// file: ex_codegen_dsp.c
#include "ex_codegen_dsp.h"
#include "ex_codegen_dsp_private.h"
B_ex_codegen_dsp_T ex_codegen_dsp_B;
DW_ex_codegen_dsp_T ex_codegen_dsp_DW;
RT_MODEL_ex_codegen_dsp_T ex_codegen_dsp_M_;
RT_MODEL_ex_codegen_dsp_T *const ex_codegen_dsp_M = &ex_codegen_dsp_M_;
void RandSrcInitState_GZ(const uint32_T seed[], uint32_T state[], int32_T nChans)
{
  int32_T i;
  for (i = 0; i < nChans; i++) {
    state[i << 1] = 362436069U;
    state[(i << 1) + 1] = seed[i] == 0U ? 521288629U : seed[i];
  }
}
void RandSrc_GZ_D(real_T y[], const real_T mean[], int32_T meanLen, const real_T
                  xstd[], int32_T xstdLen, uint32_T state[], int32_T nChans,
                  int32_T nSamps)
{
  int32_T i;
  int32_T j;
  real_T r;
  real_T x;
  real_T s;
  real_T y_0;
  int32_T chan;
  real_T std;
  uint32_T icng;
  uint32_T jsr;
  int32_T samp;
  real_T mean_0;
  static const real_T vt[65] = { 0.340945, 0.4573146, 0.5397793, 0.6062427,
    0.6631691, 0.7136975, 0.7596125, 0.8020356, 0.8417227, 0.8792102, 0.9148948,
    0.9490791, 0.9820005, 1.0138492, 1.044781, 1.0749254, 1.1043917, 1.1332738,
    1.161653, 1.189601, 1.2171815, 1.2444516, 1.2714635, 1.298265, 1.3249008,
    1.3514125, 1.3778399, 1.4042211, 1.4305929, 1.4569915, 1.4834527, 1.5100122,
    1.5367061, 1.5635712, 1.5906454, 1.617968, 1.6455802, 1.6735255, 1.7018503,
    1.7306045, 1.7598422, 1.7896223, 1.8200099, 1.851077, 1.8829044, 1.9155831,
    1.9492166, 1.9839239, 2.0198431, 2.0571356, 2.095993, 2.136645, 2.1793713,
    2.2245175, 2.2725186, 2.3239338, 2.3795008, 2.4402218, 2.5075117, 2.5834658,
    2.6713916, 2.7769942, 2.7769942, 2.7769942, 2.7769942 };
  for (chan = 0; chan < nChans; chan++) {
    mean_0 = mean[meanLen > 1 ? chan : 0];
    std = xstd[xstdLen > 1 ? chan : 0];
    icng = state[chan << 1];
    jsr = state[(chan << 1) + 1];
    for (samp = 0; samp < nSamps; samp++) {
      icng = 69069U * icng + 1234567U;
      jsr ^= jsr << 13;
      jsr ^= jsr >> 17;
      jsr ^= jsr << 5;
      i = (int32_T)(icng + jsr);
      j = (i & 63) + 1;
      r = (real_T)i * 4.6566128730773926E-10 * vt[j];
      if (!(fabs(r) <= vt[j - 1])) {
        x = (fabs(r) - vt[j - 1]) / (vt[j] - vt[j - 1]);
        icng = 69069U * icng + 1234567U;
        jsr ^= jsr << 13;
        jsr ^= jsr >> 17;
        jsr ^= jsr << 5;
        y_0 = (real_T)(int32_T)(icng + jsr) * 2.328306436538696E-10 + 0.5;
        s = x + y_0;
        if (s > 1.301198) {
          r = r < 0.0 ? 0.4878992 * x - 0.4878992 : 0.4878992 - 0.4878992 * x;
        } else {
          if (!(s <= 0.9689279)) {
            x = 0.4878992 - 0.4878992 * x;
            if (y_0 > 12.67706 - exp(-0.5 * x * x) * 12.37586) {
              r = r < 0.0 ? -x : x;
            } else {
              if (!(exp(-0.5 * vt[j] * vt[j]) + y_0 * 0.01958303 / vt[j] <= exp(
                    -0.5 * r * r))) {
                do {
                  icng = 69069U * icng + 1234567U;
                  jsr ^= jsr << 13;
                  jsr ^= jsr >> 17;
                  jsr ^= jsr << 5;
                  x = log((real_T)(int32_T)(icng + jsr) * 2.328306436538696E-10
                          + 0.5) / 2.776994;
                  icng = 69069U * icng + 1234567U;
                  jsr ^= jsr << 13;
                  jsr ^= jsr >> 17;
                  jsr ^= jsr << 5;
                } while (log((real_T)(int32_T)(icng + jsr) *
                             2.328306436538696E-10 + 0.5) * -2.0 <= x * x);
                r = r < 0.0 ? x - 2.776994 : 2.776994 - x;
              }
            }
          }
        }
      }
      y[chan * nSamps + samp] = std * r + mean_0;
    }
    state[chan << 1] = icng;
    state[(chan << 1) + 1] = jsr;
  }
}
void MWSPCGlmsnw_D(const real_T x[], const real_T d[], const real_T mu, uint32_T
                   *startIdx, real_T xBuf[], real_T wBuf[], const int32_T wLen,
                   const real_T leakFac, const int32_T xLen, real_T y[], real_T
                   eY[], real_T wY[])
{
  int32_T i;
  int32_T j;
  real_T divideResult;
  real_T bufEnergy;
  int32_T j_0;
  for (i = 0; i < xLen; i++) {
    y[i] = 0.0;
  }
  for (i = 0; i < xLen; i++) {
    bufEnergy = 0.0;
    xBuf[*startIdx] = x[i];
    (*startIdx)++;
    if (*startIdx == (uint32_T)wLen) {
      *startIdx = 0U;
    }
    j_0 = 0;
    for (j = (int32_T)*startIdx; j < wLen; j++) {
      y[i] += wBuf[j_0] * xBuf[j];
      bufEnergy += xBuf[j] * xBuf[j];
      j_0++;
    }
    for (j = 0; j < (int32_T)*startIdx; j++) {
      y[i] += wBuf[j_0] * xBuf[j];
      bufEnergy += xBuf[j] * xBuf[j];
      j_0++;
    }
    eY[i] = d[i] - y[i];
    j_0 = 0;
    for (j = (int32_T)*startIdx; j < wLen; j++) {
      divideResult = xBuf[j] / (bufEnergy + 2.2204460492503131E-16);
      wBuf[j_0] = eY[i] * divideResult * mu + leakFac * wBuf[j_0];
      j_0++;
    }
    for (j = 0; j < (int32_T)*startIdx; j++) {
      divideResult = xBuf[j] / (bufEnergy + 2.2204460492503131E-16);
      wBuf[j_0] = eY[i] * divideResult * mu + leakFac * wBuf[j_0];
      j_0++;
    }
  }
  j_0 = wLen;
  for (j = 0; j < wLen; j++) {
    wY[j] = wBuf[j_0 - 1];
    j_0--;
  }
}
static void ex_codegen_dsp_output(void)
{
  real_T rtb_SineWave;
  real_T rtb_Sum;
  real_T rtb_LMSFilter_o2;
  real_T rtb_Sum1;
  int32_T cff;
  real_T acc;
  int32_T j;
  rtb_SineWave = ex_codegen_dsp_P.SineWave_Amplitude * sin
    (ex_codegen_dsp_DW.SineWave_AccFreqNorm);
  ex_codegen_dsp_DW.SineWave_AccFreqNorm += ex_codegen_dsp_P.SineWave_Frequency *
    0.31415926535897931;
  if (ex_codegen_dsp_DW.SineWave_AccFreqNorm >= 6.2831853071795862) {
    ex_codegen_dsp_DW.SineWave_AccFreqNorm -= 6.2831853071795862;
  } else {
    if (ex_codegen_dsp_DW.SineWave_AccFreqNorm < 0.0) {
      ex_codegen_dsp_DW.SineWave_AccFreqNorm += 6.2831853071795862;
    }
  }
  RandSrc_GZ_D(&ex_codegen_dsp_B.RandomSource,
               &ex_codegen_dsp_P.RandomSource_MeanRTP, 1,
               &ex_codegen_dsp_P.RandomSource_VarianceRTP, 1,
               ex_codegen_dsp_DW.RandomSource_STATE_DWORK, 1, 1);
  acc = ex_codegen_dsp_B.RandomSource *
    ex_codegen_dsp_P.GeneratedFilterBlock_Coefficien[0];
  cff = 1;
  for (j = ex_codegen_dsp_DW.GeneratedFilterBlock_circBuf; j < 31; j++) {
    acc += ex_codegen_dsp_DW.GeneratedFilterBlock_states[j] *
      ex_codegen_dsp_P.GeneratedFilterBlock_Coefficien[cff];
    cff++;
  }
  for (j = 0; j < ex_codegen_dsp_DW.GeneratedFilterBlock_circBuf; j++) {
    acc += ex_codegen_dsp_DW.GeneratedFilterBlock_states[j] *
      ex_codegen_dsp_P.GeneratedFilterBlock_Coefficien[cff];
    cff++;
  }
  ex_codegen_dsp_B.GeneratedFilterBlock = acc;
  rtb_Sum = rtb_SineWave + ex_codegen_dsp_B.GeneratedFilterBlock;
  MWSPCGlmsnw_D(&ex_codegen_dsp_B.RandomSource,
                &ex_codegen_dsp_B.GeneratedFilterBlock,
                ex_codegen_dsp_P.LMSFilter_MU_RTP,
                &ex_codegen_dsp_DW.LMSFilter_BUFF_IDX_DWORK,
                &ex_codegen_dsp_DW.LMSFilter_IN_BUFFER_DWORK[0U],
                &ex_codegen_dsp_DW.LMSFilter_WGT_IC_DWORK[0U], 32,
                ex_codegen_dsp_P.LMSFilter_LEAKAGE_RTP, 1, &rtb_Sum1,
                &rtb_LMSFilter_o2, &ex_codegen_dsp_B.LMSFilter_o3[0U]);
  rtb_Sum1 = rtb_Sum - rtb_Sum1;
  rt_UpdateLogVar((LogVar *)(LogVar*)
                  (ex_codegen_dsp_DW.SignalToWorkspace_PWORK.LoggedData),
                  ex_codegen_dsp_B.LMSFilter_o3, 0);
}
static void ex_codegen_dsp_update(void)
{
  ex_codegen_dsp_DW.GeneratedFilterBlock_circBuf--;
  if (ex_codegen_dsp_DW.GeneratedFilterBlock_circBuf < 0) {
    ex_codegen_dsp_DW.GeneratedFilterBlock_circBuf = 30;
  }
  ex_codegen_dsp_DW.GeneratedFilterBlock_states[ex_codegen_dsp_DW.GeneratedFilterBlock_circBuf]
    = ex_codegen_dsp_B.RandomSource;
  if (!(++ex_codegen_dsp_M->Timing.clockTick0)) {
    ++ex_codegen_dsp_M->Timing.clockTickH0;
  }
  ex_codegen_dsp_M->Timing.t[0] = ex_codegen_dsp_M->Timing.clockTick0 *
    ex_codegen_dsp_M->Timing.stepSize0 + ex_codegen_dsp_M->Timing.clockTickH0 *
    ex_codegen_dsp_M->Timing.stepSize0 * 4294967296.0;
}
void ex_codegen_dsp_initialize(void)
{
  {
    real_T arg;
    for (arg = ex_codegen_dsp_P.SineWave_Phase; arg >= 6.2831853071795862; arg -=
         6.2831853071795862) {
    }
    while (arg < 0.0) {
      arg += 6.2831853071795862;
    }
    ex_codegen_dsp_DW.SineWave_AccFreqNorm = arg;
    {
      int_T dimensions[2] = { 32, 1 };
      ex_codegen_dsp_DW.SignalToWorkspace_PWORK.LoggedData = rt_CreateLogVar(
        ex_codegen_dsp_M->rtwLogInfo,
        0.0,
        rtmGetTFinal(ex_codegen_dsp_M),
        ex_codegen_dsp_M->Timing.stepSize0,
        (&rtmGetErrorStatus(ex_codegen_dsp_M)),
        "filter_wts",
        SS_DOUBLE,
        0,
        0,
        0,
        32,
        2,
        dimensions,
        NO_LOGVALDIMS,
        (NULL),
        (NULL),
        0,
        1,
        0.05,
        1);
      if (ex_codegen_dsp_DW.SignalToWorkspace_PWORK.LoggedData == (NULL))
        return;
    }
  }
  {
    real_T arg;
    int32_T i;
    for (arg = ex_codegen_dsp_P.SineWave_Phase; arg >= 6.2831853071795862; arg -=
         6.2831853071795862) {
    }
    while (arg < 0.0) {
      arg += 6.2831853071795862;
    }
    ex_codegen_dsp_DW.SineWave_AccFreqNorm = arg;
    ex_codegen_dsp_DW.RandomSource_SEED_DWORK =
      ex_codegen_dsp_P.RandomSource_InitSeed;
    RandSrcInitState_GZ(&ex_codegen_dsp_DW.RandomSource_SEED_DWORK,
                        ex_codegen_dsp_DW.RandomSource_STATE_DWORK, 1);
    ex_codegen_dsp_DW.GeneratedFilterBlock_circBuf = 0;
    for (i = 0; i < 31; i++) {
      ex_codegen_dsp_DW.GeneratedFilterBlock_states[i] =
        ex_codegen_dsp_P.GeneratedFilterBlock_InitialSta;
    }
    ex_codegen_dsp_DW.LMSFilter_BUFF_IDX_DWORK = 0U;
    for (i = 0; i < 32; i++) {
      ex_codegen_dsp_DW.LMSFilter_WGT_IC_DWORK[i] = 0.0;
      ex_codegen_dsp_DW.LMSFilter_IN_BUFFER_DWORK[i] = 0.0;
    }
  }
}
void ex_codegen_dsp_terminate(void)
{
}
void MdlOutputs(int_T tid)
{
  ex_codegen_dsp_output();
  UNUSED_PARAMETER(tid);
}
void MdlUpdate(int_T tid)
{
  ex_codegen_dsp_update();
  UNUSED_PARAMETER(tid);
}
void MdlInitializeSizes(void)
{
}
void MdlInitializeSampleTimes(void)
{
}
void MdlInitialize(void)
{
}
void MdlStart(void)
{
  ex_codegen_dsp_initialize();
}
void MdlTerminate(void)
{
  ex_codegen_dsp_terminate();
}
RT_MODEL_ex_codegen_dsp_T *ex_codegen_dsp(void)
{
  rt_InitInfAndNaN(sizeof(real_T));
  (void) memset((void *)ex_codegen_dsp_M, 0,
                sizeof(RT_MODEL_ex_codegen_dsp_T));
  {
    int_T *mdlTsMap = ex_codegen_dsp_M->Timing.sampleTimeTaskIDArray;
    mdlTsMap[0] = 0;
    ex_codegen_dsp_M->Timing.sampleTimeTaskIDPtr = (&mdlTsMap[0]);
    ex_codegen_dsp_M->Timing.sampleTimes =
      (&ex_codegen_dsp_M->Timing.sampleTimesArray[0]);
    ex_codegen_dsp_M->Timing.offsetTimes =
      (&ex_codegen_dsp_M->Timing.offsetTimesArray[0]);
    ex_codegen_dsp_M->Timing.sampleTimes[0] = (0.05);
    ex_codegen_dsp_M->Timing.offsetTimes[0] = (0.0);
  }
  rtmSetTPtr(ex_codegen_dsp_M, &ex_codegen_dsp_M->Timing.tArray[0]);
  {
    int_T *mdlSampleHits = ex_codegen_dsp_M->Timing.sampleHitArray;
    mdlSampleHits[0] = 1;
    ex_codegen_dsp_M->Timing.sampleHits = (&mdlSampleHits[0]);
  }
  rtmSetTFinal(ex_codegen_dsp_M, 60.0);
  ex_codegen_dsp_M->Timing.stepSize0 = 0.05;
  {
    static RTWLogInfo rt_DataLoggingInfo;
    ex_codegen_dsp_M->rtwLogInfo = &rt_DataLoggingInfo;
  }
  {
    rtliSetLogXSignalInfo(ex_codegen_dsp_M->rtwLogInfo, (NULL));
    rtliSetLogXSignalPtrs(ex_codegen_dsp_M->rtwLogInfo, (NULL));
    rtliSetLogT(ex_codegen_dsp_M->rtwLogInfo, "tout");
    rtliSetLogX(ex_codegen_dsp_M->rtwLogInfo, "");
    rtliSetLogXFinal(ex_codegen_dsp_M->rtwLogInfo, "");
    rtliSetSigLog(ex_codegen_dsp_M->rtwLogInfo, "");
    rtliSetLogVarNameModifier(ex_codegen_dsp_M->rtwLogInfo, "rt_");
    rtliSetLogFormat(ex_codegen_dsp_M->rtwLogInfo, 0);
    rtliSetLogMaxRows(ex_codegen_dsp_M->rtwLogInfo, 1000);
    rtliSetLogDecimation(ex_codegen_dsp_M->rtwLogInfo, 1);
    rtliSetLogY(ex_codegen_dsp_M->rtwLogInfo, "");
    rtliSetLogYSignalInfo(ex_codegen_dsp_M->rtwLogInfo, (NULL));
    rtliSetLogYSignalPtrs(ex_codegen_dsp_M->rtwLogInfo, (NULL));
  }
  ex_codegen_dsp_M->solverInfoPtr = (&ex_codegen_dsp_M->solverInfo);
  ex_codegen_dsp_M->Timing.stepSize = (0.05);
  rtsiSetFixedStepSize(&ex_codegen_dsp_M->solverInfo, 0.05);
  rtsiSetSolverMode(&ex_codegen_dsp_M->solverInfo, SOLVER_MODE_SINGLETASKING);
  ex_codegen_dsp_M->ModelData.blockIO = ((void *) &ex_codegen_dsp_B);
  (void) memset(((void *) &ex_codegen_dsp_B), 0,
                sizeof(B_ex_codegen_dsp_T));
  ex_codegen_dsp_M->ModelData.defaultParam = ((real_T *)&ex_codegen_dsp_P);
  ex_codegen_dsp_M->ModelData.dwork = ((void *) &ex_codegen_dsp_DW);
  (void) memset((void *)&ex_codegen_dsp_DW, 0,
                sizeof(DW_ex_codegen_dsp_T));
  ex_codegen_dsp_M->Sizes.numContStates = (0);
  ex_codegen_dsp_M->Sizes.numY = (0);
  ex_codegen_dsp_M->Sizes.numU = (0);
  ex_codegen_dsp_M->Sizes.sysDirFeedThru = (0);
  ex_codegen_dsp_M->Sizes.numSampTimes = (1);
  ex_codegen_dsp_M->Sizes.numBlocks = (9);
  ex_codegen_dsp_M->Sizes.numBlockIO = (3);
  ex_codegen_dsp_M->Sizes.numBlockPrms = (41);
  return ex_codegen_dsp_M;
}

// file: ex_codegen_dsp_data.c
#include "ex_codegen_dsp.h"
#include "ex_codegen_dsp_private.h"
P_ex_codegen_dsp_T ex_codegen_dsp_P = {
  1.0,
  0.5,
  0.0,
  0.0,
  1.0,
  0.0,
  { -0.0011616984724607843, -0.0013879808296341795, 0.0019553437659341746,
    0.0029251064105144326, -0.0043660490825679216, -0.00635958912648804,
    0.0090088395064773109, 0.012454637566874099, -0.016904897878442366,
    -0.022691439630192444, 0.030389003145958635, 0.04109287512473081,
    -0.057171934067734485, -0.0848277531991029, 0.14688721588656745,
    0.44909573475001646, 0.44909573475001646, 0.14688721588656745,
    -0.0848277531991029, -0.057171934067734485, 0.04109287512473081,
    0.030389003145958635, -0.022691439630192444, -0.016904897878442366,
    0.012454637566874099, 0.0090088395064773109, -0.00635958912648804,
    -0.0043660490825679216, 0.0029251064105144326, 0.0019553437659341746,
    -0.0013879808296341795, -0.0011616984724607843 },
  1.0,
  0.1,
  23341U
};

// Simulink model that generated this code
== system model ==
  VectorScope#1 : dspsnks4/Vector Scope  <- 1: LMSFilter/3
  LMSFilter : dspadpt3/LMS Filter  <- 1: RandomSource, 2: GeneratedFilterBlock
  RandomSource : dspsrcs4/Random Source
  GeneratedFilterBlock : DiscreteFir  <- 1: RandomSource
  Sum1 : Sum  Inputs=+-  <- 1: Sum, 2: LMSFilter
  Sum : Sum  Inputs=++  <- 1: SineWave, 2: GeneratedFilterBlock
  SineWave : dspsrcs4/Sine Wave  Amplitude=1  Frequency=0.5  Phase=0
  SignalToWorkspace : SignalToWorkspace  <- 1: LMSFilter/3
